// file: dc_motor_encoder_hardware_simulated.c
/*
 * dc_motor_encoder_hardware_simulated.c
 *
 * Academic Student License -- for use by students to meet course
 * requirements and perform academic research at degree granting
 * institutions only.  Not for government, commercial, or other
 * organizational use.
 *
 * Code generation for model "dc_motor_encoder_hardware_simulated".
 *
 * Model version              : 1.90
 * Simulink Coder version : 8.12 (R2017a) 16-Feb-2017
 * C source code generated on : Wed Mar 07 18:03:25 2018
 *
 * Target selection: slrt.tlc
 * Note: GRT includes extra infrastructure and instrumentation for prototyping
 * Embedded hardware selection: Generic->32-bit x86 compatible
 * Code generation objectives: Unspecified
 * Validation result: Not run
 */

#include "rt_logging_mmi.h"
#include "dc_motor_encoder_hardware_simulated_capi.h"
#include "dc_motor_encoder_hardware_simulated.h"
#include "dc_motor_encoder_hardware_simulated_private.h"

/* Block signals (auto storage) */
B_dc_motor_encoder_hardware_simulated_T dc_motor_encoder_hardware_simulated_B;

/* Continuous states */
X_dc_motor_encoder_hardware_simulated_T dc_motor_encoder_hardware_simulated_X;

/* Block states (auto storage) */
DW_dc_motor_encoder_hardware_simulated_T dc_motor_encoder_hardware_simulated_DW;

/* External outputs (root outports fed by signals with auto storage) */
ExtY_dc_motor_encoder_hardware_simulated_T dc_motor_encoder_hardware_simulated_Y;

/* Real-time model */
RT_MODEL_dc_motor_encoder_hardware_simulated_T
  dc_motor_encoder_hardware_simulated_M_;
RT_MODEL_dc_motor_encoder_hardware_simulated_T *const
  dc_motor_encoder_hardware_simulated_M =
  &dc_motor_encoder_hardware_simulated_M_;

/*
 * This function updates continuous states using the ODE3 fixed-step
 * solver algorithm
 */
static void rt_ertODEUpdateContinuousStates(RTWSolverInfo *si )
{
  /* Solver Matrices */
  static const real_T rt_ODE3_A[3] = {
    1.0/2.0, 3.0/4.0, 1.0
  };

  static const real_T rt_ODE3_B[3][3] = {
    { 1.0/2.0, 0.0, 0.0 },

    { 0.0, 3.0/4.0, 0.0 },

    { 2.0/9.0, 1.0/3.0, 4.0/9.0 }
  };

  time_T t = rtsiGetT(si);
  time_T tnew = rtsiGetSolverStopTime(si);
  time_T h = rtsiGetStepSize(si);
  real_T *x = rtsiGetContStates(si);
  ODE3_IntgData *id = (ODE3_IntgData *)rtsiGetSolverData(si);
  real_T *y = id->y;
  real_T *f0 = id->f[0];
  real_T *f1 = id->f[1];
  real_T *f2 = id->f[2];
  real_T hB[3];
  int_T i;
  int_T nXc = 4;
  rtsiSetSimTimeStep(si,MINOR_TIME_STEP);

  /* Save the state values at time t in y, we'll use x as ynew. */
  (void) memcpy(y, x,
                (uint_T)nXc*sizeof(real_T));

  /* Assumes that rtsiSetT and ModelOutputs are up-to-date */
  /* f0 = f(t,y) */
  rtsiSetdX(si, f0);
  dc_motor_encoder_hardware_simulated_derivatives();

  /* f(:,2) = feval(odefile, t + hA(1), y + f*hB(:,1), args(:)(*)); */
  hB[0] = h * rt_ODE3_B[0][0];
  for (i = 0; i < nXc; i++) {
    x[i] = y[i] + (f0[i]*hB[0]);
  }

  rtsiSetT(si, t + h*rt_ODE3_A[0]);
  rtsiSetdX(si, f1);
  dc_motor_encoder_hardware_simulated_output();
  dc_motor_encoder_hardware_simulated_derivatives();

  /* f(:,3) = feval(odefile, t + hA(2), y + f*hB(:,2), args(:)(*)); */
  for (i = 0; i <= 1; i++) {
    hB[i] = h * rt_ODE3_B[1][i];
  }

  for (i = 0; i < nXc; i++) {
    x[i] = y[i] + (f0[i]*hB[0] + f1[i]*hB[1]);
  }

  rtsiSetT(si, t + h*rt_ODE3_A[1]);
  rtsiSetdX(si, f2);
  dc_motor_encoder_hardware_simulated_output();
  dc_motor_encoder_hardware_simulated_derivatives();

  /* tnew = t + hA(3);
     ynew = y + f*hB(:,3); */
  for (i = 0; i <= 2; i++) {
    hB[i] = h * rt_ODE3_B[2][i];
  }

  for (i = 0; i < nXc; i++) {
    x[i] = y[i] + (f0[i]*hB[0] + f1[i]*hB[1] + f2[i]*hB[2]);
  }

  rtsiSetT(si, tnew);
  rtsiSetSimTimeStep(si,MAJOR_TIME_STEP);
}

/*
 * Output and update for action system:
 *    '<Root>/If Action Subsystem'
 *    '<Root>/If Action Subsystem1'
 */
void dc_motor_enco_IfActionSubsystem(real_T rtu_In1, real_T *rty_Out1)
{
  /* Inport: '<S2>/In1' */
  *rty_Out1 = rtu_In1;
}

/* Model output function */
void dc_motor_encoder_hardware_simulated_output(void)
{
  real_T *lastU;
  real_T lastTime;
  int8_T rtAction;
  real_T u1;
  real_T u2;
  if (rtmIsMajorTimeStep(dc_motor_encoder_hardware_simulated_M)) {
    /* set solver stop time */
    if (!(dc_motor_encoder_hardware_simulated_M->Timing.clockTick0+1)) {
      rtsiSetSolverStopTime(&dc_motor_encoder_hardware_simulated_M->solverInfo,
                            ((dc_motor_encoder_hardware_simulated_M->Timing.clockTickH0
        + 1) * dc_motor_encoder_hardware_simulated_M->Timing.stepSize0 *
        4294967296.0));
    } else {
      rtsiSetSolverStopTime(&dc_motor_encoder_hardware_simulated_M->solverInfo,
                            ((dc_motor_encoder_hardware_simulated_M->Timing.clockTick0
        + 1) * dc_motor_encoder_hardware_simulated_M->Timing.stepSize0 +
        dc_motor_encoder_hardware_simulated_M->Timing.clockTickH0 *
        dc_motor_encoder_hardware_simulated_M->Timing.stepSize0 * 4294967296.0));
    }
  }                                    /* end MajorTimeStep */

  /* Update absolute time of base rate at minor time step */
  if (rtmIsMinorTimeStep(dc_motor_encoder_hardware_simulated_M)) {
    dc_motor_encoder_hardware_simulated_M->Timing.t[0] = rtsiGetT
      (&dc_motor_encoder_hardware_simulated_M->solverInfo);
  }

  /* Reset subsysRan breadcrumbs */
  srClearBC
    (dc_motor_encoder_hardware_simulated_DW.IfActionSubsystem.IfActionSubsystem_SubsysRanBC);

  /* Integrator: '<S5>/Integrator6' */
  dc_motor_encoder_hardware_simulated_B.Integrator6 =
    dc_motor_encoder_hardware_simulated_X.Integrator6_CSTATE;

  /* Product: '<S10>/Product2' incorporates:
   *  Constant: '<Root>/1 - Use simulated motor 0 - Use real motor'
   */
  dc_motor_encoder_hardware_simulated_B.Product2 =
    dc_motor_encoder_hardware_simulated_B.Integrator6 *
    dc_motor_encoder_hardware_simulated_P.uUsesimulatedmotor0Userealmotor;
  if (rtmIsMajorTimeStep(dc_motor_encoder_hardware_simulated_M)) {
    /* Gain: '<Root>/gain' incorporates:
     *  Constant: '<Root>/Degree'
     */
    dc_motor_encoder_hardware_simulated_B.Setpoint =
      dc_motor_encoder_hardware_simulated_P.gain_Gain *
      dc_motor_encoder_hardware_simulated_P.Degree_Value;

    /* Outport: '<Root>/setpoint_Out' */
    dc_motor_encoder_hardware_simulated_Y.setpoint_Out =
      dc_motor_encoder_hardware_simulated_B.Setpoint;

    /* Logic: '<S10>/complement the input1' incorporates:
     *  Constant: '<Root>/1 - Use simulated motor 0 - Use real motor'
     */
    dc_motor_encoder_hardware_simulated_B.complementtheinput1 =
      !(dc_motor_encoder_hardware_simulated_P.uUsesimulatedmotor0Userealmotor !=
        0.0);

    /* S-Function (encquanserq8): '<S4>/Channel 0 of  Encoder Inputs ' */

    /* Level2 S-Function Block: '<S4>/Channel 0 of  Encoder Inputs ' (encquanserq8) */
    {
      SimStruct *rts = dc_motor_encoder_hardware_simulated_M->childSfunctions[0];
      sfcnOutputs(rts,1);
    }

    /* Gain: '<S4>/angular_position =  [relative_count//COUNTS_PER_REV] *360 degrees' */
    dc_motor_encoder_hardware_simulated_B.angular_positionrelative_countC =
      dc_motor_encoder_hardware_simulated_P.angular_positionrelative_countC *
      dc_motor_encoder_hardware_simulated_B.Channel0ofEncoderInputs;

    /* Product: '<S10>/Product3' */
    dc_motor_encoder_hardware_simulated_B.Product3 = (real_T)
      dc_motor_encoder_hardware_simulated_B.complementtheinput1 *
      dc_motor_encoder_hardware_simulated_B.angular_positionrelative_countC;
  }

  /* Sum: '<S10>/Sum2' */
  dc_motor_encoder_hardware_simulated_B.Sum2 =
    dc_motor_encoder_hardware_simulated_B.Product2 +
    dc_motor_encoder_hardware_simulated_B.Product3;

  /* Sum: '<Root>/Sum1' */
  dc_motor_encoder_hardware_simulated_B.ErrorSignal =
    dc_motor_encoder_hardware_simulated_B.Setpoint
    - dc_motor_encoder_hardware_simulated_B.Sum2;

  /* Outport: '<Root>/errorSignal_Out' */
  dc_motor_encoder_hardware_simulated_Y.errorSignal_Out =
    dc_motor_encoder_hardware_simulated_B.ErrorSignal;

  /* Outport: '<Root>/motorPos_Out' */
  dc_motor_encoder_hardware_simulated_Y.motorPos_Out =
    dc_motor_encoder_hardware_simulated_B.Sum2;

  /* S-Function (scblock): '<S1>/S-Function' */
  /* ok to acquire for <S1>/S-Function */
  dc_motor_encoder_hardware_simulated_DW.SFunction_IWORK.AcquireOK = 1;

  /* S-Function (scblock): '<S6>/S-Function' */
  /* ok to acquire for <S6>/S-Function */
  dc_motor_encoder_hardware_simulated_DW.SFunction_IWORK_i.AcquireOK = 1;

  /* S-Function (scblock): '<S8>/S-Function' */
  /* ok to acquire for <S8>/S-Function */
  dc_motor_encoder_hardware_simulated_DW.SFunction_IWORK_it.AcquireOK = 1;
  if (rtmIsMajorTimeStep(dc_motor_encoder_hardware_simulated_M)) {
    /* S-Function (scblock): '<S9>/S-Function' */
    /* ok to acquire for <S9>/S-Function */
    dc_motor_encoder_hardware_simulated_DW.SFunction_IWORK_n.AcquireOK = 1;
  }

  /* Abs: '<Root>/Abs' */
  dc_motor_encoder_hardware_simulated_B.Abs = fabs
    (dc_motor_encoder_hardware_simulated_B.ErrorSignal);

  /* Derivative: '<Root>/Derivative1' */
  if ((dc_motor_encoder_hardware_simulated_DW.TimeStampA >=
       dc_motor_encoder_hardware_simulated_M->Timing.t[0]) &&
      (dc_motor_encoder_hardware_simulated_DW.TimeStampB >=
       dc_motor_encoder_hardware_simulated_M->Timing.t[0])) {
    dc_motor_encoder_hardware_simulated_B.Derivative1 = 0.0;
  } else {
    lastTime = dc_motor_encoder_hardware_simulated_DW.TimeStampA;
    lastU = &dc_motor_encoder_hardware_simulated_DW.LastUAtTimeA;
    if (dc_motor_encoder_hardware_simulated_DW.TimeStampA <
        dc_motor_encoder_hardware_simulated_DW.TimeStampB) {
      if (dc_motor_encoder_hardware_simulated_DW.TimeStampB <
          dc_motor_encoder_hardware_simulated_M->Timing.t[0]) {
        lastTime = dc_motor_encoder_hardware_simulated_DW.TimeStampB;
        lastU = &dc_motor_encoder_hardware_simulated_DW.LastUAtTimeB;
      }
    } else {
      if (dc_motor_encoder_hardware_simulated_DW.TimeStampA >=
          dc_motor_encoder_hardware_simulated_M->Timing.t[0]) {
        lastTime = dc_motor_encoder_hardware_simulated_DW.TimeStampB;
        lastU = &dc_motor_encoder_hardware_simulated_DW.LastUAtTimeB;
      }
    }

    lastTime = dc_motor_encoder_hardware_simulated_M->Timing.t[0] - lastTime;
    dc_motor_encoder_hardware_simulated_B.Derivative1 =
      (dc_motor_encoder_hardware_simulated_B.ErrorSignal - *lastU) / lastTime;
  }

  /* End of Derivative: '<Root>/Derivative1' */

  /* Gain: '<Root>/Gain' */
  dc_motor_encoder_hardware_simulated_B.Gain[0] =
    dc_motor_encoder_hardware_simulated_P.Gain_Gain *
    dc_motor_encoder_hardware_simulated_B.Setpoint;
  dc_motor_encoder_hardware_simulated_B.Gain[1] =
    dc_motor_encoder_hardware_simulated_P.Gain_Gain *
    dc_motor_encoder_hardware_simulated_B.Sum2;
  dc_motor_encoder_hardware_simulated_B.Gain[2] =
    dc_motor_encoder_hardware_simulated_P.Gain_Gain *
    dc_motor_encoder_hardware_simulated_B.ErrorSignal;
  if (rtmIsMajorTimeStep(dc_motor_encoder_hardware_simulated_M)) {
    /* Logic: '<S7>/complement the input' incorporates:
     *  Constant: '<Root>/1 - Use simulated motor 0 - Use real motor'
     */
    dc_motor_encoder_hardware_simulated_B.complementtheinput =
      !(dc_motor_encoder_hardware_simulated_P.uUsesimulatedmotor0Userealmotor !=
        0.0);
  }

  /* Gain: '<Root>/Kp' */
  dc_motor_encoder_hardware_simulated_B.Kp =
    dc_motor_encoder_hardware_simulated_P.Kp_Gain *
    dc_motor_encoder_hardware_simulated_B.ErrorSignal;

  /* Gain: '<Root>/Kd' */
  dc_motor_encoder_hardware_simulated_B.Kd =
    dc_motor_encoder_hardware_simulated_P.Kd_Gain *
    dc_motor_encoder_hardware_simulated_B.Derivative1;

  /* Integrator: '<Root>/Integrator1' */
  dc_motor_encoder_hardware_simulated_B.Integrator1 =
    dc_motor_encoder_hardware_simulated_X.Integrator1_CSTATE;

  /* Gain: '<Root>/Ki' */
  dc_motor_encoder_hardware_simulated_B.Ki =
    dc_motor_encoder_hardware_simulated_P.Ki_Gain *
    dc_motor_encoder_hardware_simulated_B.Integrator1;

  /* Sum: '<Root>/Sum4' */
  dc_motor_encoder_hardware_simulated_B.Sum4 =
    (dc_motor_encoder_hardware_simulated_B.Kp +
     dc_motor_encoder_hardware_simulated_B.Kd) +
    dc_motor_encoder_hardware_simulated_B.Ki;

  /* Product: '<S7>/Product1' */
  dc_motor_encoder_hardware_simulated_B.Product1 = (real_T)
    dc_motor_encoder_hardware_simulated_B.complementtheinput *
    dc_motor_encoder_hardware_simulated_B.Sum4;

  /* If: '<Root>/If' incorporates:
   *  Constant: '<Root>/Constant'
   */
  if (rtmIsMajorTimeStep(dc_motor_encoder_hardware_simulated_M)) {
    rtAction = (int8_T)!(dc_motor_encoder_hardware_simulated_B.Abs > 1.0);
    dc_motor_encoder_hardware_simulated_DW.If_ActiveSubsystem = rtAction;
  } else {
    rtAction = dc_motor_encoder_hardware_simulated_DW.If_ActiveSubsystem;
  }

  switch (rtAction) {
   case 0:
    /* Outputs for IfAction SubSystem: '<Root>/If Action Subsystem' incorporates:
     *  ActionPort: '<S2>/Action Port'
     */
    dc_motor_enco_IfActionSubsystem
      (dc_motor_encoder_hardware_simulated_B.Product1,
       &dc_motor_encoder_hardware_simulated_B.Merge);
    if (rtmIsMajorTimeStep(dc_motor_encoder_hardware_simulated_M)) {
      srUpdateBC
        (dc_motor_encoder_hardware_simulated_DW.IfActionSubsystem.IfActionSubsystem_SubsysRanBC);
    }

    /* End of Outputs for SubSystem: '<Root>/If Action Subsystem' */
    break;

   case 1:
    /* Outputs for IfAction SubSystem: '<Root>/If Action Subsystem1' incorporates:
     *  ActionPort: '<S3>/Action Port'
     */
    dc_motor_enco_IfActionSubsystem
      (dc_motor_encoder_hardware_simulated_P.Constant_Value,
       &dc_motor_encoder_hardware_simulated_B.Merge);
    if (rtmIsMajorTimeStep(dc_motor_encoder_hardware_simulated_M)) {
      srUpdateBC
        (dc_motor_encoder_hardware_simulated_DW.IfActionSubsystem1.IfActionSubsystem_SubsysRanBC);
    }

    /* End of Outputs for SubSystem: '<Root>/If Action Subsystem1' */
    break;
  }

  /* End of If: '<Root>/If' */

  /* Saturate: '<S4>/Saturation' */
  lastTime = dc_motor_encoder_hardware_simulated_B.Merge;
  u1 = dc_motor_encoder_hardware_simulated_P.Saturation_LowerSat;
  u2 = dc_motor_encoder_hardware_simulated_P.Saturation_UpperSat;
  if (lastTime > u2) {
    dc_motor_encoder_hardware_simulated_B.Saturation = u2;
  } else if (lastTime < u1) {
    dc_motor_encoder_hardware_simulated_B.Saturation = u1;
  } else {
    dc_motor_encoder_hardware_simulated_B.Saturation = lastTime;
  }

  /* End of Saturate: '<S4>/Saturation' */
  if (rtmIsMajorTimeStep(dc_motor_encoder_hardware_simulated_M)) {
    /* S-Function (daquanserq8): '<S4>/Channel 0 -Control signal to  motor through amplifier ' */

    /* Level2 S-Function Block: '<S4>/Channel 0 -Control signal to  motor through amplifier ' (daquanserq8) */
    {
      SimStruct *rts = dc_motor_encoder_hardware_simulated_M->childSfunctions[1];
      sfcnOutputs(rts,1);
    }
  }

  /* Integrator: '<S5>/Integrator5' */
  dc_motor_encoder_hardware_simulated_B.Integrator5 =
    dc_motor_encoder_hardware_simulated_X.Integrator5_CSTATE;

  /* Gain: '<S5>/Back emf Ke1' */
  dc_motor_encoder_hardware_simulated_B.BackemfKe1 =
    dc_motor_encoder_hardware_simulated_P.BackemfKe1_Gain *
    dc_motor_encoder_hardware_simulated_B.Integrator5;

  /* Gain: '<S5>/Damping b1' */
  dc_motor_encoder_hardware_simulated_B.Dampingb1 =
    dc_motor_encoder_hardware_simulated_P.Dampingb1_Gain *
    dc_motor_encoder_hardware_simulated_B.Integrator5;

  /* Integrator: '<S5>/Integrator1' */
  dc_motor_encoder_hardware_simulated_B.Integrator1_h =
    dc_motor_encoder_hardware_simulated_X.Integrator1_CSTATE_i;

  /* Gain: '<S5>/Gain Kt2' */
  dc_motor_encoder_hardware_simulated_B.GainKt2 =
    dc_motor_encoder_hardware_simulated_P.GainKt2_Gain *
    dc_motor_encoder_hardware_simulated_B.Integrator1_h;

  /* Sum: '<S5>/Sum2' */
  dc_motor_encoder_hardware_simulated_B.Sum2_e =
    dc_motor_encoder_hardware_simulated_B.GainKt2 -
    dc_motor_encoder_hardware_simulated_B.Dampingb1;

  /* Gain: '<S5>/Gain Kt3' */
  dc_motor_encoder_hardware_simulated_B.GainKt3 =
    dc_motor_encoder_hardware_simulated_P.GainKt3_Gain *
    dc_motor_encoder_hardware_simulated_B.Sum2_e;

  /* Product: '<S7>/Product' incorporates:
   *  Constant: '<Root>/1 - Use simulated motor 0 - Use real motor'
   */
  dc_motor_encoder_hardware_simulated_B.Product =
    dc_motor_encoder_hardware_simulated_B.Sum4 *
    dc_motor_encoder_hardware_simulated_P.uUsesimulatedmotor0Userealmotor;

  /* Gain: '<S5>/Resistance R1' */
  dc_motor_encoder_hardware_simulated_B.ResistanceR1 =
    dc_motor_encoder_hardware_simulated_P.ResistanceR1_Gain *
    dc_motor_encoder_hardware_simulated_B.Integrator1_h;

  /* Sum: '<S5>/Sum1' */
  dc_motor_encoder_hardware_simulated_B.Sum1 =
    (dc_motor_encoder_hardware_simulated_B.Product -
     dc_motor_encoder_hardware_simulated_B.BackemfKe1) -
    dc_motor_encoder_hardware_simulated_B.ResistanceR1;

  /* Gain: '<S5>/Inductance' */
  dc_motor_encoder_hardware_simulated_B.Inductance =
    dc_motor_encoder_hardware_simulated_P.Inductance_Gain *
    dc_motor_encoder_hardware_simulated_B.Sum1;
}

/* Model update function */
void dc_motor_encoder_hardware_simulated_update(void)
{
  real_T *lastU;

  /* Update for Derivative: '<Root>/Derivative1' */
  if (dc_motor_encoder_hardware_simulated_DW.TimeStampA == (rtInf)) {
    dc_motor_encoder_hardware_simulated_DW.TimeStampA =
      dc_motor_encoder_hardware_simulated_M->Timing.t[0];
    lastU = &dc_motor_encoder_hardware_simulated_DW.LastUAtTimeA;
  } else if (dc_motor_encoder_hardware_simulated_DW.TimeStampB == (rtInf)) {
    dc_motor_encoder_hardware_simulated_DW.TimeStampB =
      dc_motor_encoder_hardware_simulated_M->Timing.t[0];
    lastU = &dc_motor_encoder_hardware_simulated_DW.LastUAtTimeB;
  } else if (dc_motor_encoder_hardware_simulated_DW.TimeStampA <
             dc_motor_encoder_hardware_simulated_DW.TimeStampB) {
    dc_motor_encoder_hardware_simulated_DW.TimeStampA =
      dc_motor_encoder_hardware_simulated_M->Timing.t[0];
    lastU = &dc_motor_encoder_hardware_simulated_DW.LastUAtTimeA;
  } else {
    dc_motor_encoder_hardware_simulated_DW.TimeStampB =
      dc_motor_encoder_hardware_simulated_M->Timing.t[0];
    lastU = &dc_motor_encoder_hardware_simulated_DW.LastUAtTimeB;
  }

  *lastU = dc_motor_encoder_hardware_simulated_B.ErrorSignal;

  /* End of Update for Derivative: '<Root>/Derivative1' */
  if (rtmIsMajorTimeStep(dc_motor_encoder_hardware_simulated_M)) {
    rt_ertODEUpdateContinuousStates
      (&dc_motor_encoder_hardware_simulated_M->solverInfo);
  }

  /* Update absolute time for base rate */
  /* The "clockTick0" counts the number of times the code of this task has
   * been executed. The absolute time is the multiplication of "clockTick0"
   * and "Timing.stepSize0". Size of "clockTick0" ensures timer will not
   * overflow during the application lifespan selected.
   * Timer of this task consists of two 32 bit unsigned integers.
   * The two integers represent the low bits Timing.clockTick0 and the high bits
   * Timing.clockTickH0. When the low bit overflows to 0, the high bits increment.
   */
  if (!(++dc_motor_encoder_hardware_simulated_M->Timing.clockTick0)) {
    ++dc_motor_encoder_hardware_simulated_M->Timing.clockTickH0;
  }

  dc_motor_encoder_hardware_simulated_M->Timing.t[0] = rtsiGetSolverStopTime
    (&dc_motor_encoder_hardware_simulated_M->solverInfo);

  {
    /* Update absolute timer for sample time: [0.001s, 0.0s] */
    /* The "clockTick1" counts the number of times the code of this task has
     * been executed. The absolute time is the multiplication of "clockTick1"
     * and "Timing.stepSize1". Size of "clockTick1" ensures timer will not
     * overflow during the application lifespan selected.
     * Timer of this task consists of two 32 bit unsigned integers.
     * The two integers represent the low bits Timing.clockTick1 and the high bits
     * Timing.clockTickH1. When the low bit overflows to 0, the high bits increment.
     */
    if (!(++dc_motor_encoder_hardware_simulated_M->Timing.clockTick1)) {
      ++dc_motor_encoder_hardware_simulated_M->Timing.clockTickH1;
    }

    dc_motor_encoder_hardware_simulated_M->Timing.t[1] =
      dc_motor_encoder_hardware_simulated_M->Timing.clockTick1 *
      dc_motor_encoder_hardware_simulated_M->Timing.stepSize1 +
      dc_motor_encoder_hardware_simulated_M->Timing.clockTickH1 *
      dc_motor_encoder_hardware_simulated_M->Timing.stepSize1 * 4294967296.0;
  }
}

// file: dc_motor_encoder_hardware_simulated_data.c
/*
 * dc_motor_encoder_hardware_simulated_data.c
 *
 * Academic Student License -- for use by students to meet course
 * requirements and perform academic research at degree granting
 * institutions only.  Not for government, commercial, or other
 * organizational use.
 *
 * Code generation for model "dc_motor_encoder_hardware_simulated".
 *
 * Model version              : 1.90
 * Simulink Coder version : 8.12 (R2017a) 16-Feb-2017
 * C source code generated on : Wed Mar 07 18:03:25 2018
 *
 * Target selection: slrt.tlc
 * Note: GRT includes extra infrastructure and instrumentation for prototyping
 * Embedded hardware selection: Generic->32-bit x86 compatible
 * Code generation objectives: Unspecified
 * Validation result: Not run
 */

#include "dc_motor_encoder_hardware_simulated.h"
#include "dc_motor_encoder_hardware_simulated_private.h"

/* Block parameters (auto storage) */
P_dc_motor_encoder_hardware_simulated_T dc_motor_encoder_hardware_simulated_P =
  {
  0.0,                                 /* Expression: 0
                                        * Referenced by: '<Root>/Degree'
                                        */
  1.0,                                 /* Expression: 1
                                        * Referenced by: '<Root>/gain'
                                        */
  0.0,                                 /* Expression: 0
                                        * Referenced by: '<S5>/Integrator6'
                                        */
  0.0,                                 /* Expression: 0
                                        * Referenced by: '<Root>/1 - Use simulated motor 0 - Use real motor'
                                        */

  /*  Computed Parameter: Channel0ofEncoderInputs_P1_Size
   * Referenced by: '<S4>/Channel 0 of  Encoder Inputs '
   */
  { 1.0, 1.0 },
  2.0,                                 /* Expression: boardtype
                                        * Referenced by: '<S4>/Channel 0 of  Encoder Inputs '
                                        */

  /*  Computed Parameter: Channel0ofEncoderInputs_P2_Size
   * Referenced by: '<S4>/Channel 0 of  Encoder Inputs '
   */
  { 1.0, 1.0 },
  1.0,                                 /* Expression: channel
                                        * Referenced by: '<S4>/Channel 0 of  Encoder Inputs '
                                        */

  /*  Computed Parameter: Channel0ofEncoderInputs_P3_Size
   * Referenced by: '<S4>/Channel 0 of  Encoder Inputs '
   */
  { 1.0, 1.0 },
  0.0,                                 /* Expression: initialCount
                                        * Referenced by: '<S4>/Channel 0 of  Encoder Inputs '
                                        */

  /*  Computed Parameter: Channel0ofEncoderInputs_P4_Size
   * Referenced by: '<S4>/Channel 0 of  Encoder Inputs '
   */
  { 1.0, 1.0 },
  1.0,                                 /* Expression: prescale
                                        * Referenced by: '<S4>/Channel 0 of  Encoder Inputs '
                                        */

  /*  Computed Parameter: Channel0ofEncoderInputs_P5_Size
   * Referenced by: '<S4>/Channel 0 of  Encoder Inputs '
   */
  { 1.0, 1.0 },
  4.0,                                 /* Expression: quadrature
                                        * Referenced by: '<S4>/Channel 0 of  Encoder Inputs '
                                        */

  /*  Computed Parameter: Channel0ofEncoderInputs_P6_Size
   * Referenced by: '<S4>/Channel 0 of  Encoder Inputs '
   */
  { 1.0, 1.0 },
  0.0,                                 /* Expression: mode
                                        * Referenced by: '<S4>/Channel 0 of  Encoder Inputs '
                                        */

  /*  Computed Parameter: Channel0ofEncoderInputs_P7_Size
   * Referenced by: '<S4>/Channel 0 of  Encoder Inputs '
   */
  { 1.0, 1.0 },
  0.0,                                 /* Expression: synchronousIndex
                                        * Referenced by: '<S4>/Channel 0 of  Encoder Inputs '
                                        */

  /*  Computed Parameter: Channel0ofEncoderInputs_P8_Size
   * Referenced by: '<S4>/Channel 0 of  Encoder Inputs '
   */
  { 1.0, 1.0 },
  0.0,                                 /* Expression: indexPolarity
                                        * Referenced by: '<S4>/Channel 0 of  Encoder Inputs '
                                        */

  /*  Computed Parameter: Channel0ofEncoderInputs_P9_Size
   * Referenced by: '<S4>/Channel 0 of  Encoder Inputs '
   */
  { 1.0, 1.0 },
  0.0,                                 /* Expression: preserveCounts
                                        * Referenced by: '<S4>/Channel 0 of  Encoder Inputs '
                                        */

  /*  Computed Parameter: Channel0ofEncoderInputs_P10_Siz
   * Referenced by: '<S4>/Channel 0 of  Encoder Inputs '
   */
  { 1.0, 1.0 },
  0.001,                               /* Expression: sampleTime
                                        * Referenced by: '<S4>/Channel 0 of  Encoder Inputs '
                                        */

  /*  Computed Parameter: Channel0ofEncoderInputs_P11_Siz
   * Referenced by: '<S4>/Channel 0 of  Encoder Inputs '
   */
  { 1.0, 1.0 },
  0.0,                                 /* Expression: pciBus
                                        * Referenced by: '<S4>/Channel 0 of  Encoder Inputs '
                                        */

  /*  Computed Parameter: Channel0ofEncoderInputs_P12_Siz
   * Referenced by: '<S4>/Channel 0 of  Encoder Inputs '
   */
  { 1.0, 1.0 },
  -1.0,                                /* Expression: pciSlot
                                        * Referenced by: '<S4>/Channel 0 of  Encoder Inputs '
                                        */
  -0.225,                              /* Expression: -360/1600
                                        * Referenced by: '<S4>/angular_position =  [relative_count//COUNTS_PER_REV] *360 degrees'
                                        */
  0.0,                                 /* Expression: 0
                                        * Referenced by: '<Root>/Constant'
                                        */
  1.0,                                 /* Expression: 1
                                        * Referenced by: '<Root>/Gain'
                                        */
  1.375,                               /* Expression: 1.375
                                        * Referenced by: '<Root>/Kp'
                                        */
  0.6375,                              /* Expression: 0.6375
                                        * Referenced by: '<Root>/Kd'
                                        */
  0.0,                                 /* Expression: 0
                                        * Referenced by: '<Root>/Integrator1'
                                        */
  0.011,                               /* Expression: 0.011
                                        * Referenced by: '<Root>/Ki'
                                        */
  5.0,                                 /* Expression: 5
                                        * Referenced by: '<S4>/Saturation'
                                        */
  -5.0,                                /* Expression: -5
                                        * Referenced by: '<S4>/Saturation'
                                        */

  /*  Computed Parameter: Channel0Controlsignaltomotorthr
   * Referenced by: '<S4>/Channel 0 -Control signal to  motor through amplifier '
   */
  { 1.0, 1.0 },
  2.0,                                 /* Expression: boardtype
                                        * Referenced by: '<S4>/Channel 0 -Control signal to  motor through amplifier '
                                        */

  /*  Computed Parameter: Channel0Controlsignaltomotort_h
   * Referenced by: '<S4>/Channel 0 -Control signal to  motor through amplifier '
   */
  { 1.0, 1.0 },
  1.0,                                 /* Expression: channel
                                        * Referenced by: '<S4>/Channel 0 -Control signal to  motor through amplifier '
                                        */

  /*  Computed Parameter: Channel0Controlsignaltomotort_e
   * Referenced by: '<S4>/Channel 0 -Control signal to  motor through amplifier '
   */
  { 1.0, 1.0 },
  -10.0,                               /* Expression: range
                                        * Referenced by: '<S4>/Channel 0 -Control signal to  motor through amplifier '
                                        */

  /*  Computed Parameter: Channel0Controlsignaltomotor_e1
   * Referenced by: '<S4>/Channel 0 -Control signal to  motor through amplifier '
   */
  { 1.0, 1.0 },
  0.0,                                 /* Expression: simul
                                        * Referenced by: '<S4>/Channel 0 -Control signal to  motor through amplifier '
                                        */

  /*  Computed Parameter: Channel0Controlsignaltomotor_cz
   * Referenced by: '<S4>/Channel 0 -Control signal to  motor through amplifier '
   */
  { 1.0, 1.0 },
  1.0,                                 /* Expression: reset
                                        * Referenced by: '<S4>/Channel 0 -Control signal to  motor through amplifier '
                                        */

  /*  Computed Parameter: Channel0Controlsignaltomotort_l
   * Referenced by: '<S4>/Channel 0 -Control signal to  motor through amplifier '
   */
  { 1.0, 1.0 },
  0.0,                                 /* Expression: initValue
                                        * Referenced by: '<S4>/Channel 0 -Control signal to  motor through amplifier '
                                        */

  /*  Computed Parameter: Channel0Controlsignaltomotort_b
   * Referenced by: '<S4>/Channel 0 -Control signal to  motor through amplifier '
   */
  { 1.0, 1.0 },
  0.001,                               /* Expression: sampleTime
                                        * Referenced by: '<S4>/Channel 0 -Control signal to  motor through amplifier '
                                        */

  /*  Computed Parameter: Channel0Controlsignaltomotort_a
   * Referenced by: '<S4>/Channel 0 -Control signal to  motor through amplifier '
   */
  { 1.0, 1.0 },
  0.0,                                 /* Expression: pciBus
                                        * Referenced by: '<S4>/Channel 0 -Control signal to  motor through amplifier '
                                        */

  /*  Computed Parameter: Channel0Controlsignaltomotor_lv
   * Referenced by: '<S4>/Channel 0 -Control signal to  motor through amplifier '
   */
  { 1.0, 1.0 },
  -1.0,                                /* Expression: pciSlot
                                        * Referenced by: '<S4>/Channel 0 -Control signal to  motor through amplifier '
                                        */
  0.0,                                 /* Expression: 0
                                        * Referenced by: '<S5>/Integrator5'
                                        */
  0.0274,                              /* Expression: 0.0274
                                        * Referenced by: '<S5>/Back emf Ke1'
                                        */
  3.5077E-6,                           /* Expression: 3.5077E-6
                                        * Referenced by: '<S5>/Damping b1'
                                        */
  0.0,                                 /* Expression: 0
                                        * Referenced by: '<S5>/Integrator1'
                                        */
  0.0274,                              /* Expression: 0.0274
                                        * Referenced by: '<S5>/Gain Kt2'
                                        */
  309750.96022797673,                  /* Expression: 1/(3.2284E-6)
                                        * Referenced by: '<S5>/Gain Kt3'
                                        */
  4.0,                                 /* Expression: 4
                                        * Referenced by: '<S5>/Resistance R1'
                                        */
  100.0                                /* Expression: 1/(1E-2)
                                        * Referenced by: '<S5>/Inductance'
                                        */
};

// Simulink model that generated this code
simulink model "dc_motor_encoder_hardware_simulated"  (Simulink 8.9)
settings: Solver=ode3  StartTime=0.0  StopTime=inf  FixedStep=0.001  RelTol=1e-3  EnableMultiTasking=on
libraries: slrtlib x4, xpcquanserlib x2

== system dc_motor_encoder_hardware_simulated ==
  note: Adjust these gains and observe the change of the
      | motor response on the Error and Motor Position
      | plots.
  note: First, test the control inputs on the simulated motor and
      | adjust gains according to the response. Then, flip the switch and
      | test with the real motor in the loop
  note: Switch
  1 - Use simulated motor 0 - Use real motor : Constant  Value=0
  Abs : Abs
  Constant : Constant  Value=0
  Data Display : slrtlib/Displays and Logging/Scope   scopeno=3  scopetype=Target  autostart=on  viewmode=Numerical  formatstr="'Setpoint        %3.2f,Motor Position  %3.2f,Error Signal    %3.2f'"  grid=on  ylimits=[0,170]  nosamples=200  noprepostsamples=0  interleave=10  triggermode=FreeRun  triggersignal=1  trigsignalfromport=off  triggerlevel=0.0  triggerslope=Either  triggerscope=1  triggersample=0  filename=data.dat  mode=Lazy  writesize=512  autorestart=off  dynamicfilemode=off  maxwritefilesize=512*1024^2
  Degree : Constant  Value=0
  Derivative1 : Derivative
  Gain : Gain
  If : If  IfExpression=u1 > 1
  If Action Subsystem : Subsystem  TreatAsAtomicUnit=on
  If Action Subsystem1 : Subsystem  TreatAsAtomicUnit=on
  Integrator1 : Integrator
  Kd : Gain  Gain=0.6375
  Ki : Gain  Gain=0.011
  Kp : Gain  Gain=1.375
  Merge : Merge
  Mux : Mux  Inputs=3
  Real motor : Subsystem
  Simulated motor : Subsystem
  Sum1 : Sum  Inputs=|+-
  Sum4 : Sum  Inputs=||+++
  error signal : slrtlib/Displays and Logging/Scope   scopeno=2  scopetype=Target  autostart=on  viewmode=Graphical rolling  formatstr='%15.6f'  grid=on  ylimits=[-180,180]  nosamples=500  noprepostsamples=0  interleave=10  triggermode=FreeRun  triggersignal=1  trigsignalfromport=off  triggerlevel=0.0  triggerslope=Either  triggerscope=1  triggersample=0  filename=data.dat  mode=Lazy  writesize=512  autorestart=off  dynamicfilemode=off  maxwritefilesize=512*1024^2
  gain : Gain
  input side switching logic : Subsystem
  motor position : slrtlib/Displays and Logging/Scope   scopeno=7  scopetype=Target  autostart=on  viewmode=Graphical rolling  formatstr='%15.6f'  grid=on  ylimits=[-180,180]  nosamples=500  noprepostsamples=0  interleave=10  triggermode=FreeRun  triggersignal=1  trigsignalfromport=off  triggerlevel=0.0  triggerslope=Either  triggerscope=1  triggersample=0  filename=data.dat  mode=Lazy  writesize=512  autorestart=off  dynamicfilemode=off  maxwritefilesize=512*1024^2
  setpoint : slrtlib/Displays and Logging/Scope   scopeno=1  scopetype=Target  autostart=on  viewmode=Graphical rolling  formatstr='%15.6f'  grid=on  ylimits=[-180,180]  nosamples=500  noprepostsamples=0  interleave=10  triggermode=FreeRun  triggersignal=1  trigsignalfromport=off  triggerlevel=0.0  triggerslope=Either  triggerscope=1  triggersample=0  filename=data.dat  mode=Lazy  writesize=512  autorestart=off  dynamicfilemode=off  maxwritefilesize=512*1024^2
  switching logic : Subsystem
  setpoint_Out : Outport
  errorSignal_Out : Outport  Port=2
  motorPos_Out : Outport  Port=3
  wires:
  Kp/1 -> Sum4/1
  Kd/1 -> Sum4/2
  Derivative1/1 -> Kd/1
  Integrator1/1 -> Ki/1
  Ki/1 -> Sum4/3
  gain/1 -> Sum1/1, Mux/1, setpoint/1, setpoint_Out/1  "Setpoint"
  Degree/1 -> gain/1
  input side switching logic/1(Simulated) -> Simulated motor/1(control  input)
  Simulated motor/1(position) -> switching logic/1(simulated)
  Real motor/1(position in degrees) -> switching logic/3(real)
  switching logic/1(position) -> Mux/2, Sum1/2, motor position/1, motorPos_Out/1  "Motor Position"
  Sum4/1 -> input side switching logic/1(control input)
  1 - Use simulated motor 0 - Use real motor/1 -> input side switching logic/2(switch  position), switching logic/2(switch position)
  Gain/1 -> Data Display/1
  Mux/1 -> Gain/1
  Sum1/1 -> Kp/1, Derivative1/1, Integrator1/1, Abs/1, Mux/3, error signal/1, errorSignal_Out/1  "Error Signal"
  If/2 -> If Action Subsystem1/Action
  If/1 -> If Action Subsystem/Action
  Constant/1 -> If Action Subsystem1/1(In1)
  input side switching logic/2(Real) -> If Action Subsystem/1(In1)
  If Action Subsystem/1(Out1) -> Merge/1
  If Action Subsystem1/1(Out1) -> Merge/2
  Abs/1 -> If/1
  Merge/1 -> Real motor/1(unfiltered  control input)

== system dc_motor_encoder_hardware_simulated/If Action Subsystem ==
  In1 : Inport
  Action Port : ActionPort  ActionType=then
  Out1 : Outport
  wires:
  In1/1 -> Out1/1

== system dc_motor_encoder_hardware_simulated/If Action Subsystem1 ==
  In1 : Inport
  Action Port : ActionPort  ActionType=else
  Out1 : Outport
  wires:
  In1/1 -> Out1/1

== system dc_motor_encoder_hardware_simulated/Real motor ==
  note: Saturation
  note: External connections to and from the motor using the Q4.
      |
      | Encoder feedback is scaled using the modulus and Gain blocks to
      | match the range of the Desired Trajectory input.
      |
      | In this example need to convert the encoder counts to a value between 0 and COUNTS_PER_REV.
      | Further, the count obtained for that revolution needs to be scaled to an angle feedback (between
      | 0 and 360 degrees), which is the purpose of the Gain block.
  unfiltered  control input : Inport
  "Channel 0 -Control signal to  motor through amplifier " : xpcquanserlib/D//A/Q4 DA   channel=[1]  range=[-10]  simul=off  reset=[1]  initValue=[0]  sampleTime=.001  slot=-1
  "Channel 0 of  Encoder Inputs " : xpcquanserlib/Incremental Encoder/Q4 Enc   channel=[1]  initialCount=[0]  prescale=[1]  quadrature=[4]  mode=[0]  synchronousIndex=[0]  indexPolarity=[0]  preserveCounts=[0]  sampleTime=.001  slot=-1
  Saturation : Saturate  UpperLimit=5  LowerLimit=-5
  angular_position =  [relative_count/COUNTS_PER_REV] *360 degrees : Gain  Gain=-360/1600
  position in degrees : Outport
  wires:
  Saturation/1 -> "Channel 0 -Control signal to  motor through amplifier "/1
  angular_position =  [relative_count/COUNTS_PER_REV] *360 degrees/1 -> position in degrees/1
  "Channel 0 of  Encoder Inputs "/1 -> angular_position =  [relative_count/COUNTS_PER_REV] *360 degrees/1
  unfiltered  control input/1 -> Saturation/1

== system dc_motor_encoder_hardware_simulated/Simulated motor ==
  control  input : Inport
  Back emf Ke1 : Gain  Gain=0.0274
  Damping b1 : Gain  Gain=3.5077E-6
  Gain Kt2 : Gain  Gain=0.0274
  Gain Kt3 : Gain  Gain=1/(3.2284E-6)
  Inductance : Gain  Gain=1/(1E-2)
  Integrator1 : Integrator
  Integrator5 : Integrator
  Integrator6 : Integrator
  Resistance R1 : Gain  Gain=4
  Sum1 : Sum  Inputs=||+--
  Sum2 : Sum  Inputs=|+-
  position : Outport
  wires:
  Sum1/1 -> Inductance/1
  Inductance/1 -> Integrator1/1
  Integrator1/1 -> Gain Kt2/1, Resistance R1/1
  Gain Kt2/1 -> Sum2/1
  Sum2/1 -> Gain Kt3/1
  Gain Kt3/1 -> Integrator5/1
  Integrator5/1 -> Integrator6/1, Back emf Ke1/1, Damping b1/1
  Back emf Ke1/1 -> Sum1/2
  Damping b1/1 -> Sum2/2
  Resistance R1/1 -> Sum1/3
  Integrator6/1 -> position/1
  control  input/1 -> Sum1/1

== system dc_motor_encoder_hardware_simulated/input side switching logic ==
  control input : Inport
  switch  position : Inport  Port=2
  Product : Product  RndMeth=Zero
  Product1 : Product  RndMeth=Zero
  complement the input : Logic  Operator=NOT  AllPortsSameDT=off  OutDataTypeStr=boolean
  Simulated : Outport
  Real : Outport  Port=2
  wires:
  control input/1 -> Product/1, Product1/2
  complement the input/1 -> Product1/1
  switch  position/1 -> Product/2, complement the input/1
  Product/1 -> Simulated/1
  Product1/1 -> Real/1

== system dc_motor_encoder_hardware_simulated/switching logic ==
  simulated : Inport
  switch position : Inport  Port=2
  real : Inport  Port=3
  Product2 : Product  RndMeth=Zero
  Product3 : Product  RndMeth=Zero
  Sum2 : Sum  Inputs=|++
  complement the input1 : Logic  Operator=NOT  AllPortsSameDT=off  OutDataTypeStr=boolean
  position : Outport
  wires:
  complement the input1/1 -> Product3/1
  Product2/1 -> Sum2/1
  Product3/1 -> Sum2/2
  switch position/1 -> complement the input1/1, Product2/2
  simulated/1 -> Product2/1
  Sum2/1 -> position/1
  real/1 -> Product3/2
